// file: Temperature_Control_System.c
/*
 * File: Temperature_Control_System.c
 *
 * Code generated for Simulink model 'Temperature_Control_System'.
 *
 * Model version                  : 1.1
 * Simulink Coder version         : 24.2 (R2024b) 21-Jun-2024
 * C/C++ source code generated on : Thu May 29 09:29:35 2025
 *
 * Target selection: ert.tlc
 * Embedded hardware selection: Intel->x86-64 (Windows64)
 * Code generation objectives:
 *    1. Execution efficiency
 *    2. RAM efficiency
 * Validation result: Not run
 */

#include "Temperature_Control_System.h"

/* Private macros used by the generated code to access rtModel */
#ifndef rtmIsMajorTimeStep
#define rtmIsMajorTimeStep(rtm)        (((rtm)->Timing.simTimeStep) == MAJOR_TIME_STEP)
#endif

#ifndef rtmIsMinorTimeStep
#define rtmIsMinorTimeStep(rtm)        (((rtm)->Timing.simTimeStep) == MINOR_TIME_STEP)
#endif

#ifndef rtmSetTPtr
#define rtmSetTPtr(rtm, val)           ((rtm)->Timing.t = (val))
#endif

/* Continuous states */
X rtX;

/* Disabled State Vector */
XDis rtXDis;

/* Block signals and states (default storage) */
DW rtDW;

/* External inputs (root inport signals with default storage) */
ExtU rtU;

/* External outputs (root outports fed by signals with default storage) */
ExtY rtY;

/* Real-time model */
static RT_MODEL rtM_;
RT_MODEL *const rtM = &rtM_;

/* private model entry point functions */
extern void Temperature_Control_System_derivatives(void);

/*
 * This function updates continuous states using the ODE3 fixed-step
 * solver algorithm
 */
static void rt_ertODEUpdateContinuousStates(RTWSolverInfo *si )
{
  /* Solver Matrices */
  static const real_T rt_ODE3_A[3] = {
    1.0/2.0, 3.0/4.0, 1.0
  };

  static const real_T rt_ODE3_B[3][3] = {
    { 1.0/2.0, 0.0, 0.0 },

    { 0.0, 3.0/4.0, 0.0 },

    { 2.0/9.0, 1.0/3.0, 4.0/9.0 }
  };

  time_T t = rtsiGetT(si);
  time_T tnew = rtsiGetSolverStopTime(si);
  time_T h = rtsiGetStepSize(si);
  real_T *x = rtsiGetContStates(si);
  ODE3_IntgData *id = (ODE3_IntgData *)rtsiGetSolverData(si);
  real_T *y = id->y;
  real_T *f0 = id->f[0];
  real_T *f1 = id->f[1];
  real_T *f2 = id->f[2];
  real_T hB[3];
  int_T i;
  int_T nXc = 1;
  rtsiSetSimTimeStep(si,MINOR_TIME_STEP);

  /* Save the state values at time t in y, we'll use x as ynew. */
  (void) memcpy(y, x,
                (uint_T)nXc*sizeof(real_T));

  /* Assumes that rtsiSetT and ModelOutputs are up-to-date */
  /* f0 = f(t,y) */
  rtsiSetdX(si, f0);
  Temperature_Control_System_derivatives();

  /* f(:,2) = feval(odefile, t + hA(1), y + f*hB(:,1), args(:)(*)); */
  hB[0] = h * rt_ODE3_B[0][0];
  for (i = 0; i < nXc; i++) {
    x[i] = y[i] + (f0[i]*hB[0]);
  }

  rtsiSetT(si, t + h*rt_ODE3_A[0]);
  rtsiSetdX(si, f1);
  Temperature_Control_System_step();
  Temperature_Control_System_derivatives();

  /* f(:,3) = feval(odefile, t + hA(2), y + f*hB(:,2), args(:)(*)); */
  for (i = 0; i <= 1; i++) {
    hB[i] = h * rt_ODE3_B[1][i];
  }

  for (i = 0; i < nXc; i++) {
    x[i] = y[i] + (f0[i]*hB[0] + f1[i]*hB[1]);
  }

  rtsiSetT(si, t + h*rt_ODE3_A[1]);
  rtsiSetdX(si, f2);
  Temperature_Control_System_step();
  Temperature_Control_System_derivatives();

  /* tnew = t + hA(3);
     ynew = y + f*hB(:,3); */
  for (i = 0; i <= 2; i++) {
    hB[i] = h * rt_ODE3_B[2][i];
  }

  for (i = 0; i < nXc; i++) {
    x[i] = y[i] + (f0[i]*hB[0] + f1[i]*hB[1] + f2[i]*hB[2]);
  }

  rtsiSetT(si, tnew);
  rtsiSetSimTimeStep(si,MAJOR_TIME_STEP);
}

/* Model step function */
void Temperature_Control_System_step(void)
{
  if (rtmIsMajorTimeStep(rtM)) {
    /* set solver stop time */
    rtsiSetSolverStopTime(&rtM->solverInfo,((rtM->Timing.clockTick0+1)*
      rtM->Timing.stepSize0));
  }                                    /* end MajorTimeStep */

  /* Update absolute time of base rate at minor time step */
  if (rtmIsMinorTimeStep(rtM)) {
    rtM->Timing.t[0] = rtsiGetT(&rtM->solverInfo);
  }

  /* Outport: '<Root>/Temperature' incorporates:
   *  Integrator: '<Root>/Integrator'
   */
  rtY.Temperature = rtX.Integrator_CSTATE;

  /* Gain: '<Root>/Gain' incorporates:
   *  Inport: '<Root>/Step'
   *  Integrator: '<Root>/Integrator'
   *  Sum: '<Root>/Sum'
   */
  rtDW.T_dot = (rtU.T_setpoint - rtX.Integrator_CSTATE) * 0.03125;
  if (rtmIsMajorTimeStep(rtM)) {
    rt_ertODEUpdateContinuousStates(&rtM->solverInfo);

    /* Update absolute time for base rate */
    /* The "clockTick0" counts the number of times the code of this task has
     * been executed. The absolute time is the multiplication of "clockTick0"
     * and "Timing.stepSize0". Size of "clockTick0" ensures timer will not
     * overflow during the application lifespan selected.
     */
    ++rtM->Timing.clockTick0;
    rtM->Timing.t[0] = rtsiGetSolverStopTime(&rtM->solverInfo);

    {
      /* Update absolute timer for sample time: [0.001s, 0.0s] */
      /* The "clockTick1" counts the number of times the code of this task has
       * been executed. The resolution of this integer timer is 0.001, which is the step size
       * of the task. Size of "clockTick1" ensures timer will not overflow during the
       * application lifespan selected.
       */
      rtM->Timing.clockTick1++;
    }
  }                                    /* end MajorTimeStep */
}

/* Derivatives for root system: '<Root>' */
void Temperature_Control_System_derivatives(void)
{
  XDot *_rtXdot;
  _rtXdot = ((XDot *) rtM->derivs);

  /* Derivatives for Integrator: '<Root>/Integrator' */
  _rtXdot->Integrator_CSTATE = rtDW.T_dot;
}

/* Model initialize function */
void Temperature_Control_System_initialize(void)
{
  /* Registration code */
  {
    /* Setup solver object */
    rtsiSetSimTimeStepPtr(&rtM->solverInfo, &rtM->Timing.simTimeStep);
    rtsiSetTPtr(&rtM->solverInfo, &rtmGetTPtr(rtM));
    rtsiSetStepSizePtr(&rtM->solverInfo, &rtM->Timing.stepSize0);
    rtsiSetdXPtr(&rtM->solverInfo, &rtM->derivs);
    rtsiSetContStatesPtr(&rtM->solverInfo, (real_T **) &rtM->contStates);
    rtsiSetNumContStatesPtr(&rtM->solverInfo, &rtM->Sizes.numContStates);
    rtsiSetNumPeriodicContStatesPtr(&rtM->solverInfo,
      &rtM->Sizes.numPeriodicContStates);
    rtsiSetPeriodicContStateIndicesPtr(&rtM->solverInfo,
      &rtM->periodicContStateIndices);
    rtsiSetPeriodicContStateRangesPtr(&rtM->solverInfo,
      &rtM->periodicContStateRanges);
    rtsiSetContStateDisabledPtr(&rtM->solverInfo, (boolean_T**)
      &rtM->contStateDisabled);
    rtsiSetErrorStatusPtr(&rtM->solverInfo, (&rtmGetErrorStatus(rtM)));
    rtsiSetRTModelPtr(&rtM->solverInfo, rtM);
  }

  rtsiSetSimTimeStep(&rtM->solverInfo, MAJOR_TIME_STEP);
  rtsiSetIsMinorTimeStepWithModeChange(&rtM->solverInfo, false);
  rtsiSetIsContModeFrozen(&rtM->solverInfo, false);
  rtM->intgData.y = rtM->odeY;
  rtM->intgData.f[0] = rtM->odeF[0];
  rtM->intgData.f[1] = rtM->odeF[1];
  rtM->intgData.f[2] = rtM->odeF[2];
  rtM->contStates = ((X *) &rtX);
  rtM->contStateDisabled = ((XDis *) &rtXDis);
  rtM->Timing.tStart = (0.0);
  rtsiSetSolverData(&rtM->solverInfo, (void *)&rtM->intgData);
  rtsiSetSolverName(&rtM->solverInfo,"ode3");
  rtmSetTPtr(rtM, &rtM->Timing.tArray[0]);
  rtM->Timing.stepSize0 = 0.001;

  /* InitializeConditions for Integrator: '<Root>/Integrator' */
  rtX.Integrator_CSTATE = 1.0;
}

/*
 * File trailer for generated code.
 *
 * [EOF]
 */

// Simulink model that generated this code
simulink model "Temperature_Control_System"  (R2024b)
settings: Solver=FixedStepAuto  StartTime=0.0  StopTime=10.0  FixedStep=1e-3  RelTol=1e-3
values from neighbouring files (symbols this model uses):
  Ku = i*Ku    [Scripit.m]
  Taw = Taw*i*2    [Scripit.m]

== system Temperature_Control_System ==
  Step : Inport
  Gain : Gain  Gain=Ku/Taw
  Integrator : Integrator  InitialCondition=1
  Sum : Sum  Inputs=|+-
  Temperature : Outport
  wires:
  Integrator/1 -> Temperature/1, Sum/2  "T(t)"
  Step/1 -> Sum/1  "T_setpoint"
  Gain/1 -> Integrator/1  "T_dot"
  Sum/1 -> Gain/1
